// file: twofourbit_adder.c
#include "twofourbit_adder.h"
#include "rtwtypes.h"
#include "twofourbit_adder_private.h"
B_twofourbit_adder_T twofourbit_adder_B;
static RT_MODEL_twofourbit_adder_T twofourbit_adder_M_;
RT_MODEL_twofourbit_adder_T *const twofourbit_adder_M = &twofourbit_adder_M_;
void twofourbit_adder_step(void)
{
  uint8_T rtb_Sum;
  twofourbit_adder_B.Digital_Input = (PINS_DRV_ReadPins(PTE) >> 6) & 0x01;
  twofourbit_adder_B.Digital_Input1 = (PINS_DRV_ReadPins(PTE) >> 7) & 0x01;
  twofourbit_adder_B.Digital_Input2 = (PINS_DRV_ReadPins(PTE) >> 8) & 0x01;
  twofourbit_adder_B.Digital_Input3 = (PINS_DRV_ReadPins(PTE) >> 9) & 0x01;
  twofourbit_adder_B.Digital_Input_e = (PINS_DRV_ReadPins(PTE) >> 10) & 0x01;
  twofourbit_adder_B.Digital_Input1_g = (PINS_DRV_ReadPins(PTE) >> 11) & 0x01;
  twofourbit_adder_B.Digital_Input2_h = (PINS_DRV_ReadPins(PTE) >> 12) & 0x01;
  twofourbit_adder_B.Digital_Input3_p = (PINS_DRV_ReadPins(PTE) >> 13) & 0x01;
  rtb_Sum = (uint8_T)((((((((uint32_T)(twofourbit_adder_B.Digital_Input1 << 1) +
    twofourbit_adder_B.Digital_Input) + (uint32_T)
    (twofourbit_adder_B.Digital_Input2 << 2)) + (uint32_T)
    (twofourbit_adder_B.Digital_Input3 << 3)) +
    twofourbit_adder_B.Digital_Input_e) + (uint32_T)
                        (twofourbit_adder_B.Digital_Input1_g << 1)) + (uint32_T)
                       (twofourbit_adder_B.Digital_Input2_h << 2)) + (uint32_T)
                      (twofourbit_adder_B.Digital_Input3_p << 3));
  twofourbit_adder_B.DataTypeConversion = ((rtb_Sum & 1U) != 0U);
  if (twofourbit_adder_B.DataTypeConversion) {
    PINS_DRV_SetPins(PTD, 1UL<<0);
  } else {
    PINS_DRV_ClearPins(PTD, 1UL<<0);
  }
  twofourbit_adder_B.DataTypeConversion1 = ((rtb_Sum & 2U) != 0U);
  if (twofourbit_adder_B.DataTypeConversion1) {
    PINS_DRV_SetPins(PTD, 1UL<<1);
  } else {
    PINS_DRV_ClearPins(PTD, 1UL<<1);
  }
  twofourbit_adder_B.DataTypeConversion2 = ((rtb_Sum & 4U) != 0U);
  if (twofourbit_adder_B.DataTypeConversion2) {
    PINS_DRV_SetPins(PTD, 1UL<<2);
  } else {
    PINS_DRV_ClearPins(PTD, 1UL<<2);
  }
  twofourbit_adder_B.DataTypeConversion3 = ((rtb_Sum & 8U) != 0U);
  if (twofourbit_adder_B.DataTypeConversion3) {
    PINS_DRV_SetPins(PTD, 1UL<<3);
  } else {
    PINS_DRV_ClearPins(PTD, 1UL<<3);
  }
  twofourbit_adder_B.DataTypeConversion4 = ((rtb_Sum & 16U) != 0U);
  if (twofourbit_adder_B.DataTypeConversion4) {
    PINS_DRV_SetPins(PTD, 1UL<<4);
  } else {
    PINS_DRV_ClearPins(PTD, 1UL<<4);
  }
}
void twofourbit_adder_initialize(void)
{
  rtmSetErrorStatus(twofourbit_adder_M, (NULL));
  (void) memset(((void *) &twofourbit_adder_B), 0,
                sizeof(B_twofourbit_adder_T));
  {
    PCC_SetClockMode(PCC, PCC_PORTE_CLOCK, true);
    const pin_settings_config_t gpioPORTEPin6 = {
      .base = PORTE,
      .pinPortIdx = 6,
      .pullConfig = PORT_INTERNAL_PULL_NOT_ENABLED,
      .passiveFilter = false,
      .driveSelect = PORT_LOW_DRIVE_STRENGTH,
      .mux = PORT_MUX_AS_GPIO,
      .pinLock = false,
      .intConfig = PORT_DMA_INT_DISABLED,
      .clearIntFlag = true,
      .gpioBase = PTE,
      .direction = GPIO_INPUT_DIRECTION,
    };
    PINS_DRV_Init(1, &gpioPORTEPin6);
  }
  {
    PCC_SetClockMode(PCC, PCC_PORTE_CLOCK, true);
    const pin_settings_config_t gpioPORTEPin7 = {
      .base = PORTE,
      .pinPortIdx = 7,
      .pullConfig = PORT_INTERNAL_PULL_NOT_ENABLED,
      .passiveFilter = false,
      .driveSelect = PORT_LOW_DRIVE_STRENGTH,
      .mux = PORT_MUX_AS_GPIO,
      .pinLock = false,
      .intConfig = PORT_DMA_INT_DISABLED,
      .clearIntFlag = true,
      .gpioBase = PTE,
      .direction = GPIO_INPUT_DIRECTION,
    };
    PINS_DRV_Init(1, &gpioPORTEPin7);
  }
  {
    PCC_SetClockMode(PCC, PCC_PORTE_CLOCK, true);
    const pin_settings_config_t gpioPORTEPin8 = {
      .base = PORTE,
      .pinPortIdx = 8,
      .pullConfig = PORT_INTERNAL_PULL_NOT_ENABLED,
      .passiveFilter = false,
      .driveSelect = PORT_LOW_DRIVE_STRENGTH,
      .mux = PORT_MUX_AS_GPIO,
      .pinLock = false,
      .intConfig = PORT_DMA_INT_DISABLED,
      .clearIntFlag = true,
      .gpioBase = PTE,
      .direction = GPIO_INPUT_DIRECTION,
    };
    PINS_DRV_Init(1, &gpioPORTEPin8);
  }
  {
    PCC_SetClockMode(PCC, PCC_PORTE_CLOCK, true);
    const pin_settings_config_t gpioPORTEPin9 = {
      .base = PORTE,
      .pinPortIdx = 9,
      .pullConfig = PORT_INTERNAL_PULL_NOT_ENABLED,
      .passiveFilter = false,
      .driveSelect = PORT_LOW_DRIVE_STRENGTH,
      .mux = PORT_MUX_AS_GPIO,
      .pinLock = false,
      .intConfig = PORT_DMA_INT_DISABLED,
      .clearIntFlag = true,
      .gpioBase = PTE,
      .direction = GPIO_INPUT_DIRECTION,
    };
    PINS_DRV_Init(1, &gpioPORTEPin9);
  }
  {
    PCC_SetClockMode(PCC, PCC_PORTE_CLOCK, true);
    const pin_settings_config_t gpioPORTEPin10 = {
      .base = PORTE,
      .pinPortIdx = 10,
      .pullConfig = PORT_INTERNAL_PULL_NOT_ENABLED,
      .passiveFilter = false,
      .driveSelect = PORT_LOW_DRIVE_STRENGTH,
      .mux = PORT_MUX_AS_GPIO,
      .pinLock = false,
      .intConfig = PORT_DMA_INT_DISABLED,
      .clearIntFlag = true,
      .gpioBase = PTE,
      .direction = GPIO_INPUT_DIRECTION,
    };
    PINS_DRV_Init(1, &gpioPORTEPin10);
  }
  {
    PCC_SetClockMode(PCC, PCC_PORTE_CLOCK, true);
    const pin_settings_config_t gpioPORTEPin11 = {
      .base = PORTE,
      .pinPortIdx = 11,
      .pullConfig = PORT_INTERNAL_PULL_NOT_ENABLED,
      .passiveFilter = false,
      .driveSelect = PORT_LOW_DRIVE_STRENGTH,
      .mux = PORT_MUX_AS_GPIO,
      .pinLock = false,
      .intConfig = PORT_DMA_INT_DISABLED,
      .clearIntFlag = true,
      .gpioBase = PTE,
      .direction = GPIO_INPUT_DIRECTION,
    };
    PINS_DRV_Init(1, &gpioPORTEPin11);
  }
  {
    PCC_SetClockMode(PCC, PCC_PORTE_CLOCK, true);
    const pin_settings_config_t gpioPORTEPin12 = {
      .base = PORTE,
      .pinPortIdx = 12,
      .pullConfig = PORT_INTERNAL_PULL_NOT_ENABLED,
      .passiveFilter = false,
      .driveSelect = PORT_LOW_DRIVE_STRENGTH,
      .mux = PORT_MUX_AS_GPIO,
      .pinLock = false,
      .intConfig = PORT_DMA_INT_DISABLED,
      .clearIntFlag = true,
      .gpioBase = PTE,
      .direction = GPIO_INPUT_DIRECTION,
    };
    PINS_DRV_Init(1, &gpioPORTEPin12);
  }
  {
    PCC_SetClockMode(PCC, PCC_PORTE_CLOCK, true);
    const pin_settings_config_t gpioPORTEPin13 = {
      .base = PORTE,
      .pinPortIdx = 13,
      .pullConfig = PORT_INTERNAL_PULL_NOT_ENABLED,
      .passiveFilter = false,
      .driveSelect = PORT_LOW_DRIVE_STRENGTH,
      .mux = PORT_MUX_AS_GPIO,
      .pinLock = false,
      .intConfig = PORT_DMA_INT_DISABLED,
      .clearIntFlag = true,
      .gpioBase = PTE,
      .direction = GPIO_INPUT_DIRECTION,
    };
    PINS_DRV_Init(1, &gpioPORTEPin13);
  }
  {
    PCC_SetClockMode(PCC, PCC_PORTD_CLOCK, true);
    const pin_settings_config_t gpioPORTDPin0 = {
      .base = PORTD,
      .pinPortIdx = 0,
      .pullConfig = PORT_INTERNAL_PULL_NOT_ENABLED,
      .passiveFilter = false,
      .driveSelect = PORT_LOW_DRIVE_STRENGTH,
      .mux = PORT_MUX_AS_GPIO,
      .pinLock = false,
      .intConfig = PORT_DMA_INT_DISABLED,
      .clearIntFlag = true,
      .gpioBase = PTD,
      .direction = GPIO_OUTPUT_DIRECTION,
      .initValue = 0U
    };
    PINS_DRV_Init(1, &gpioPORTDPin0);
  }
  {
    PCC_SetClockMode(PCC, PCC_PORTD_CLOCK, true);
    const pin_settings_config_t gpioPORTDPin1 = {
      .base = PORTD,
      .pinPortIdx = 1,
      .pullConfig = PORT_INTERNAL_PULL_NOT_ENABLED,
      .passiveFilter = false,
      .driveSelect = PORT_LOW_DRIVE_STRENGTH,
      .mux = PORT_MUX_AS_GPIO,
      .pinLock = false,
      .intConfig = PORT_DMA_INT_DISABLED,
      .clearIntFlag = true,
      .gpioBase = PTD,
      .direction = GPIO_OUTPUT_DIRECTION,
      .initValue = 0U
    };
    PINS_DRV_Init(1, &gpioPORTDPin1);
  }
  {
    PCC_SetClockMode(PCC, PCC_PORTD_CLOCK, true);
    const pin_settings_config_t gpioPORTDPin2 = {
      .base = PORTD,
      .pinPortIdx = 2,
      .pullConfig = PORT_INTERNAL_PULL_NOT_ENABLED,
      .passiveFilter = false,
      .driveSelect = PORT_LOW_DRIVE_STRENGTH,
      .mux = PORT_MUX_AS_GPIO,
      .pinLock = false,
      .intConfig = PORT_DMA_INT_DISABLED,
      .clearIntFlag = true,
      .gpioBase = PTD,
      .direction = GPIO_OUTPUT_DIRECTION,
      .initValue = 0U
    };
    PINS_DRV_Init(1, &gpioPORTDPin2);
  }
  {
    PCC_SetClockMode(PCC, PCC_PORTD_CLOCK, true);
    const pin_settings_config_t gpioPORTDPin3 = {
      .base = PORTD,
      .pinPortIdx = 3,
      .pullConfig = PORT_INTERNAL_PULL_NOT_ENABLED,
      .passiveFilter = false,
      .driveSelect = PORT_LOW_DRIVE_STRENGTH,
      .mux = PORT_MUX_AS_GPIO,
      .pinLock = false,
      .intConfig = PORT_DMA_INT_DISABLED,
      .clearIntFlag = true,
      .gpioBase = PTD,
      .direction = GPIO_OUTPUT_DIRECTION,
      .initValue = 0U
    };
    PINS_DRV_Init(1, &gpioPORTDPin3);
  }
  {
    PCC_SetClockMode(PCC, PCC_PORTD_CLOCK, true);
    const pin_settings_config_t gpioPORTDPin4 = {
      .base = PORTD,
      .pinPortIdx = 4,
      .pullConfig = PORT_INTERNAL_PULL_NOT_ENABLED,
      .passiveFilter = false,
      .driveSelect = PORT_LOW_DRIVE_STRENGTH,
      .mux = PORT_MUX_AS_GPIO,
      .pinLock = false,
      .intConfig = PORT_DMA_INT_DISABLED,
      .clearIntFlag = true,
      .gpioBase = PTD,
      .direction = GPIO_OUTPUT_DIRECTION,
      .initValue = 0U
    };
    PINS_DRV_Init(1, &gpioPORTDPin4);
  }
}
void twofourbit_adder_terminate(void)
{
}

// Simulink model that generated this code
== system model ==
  Subsystem#1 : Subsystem  <- Trigger: FunctionCallGenerator#1
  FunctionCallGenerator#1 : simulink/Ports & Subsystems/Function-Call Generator
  MBD_S32K1xx_Config_Information#1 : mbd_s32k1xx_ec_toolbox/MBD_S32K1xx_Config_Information
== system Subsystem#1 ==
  TriggerPort#1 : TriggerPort  TriggerType=function-call
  Digital_Output#1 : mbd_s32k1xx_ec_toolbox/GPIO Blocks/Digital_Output  <- 1: DataTypeConversion
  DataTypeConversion : DataTypeConversion  <- 1: BitwiseOperator#1
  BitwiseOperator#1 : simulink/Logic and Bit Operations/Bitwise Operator  logicop=AND  BitMask=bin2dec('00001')  <- 1: Sum
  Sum : Sum  Inputs=++  <- 1: Sum#1, 2: Sum#2
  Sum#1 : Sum  Inputs=++++  <- 1: ArithShift#1, 2: ArithShift#2, 3: ArithShift#3, 4: ArithShift#4
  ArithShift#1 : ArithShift  <- 1: DataTypeConversion#1
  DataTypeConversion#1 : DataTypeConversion  <- 1: Digital_Input
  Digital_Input : mbd_s32k1xx_ec_toolbox/GPIO Blocks/Digital_Input
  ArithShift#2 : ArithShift  BitShiftNumber=1  <- 1: DataTypeConversion1
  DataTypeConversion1 : DataTypeConversion  <- 1: Digital_Input1
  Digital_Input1 : mbd_s32k1xx_ec_toolbox/GPIO Blocks/Digital_Input
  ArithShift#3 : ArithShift  BitShiftNumber=2  <- 1: DataTypeConversion2
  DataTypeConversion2 : DataTypeConversion  <- 1: Digital_Input2
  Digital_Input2 : mbd_s32k1xx_ec_toolbox/GPIO Blocks/Digital_Input
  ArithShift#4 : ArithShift  BitShiftNumber=3  <- 1: DataTypeConversion3
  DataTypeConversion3 : DataTypeConversion  <- 1: Digital_Input3
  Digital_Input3 : mbd_s32k1xx_ec_toolbox/GPIO Blocks/Digital_Input
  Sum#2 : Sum  Inputs=++++  <- 1: ArithShift#5, 2: ArithShift#6, 3: ArithShift#7, 4: ArithShift#8
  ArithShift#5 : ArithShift  <- 1: DataTypeConversion#2
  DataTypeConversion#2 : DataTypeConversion  <- 1: Digital_Input#1
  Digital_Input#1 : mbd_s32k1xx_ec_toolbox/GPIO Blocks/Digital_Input
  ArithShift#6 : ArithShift  BitShiftNumber=1  <- 1: DataTypeConversion#3
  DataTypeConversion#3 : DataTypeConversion  <- 1: Digital_Input#2
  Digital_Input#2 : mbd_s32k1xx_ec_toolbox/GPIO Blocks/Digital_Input
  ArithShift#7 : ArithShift  BitShiftNumber=2  <- 1: DataTypeConversion#4
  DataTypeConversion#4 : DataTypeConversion  <- 1: Digital_Input#3
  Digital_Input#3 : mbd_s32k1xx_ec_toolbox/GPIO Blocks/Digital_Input
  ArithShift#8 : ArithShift  BitShiftNumber=3  <- 1: DataTypeConversion#5
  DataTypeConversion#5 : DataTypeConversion  <- 1: Digital_Input#4
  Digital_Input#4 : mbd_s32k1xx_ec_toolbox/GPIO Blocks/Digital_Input
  Digital_Output#2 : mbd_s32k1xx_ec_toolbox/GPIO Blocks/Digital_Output  <- 1: DataTypeConversion#6
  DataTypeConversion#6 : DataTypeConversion  <- 1: BitwiseOperator#2
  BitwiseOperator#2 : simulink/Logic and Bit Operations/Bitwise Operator  logicop=AND  BitMask=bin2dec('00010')  <- 1: Sum
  Digital_Output#3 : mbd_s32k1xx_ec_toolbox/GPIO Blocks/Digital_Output  <- 1: DataTypeConversion#7
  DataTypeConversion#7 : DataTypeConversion  <- 1: BitwiseOperator#3
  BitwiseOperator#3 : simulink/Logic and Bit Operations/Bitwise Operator  logicop=AND  BitMask=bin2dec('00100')  <- 1: Sum
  Digital_Output#4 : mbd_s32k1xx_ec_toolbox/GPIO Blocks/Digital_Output  <- 1: DataTypeConversion#8
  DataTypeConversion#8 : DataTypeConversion  <- 1: BitwiseOperator#4
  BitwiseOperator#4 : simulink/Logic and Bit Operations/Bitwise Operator  logicop=AND  BitMask=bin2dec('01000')  <- 1: Sum
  Digital_Output#5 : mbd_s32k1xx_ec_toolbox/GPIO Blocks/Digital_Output  <- 1: DataTypeConversion4
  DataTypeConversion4 : DataTypeConversion  <- 1: BitwiseOperator#5
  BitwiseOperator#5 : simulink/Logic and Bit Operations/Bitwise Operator  logicop=AND  BitMask=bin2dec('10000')  <- 1: Sum
